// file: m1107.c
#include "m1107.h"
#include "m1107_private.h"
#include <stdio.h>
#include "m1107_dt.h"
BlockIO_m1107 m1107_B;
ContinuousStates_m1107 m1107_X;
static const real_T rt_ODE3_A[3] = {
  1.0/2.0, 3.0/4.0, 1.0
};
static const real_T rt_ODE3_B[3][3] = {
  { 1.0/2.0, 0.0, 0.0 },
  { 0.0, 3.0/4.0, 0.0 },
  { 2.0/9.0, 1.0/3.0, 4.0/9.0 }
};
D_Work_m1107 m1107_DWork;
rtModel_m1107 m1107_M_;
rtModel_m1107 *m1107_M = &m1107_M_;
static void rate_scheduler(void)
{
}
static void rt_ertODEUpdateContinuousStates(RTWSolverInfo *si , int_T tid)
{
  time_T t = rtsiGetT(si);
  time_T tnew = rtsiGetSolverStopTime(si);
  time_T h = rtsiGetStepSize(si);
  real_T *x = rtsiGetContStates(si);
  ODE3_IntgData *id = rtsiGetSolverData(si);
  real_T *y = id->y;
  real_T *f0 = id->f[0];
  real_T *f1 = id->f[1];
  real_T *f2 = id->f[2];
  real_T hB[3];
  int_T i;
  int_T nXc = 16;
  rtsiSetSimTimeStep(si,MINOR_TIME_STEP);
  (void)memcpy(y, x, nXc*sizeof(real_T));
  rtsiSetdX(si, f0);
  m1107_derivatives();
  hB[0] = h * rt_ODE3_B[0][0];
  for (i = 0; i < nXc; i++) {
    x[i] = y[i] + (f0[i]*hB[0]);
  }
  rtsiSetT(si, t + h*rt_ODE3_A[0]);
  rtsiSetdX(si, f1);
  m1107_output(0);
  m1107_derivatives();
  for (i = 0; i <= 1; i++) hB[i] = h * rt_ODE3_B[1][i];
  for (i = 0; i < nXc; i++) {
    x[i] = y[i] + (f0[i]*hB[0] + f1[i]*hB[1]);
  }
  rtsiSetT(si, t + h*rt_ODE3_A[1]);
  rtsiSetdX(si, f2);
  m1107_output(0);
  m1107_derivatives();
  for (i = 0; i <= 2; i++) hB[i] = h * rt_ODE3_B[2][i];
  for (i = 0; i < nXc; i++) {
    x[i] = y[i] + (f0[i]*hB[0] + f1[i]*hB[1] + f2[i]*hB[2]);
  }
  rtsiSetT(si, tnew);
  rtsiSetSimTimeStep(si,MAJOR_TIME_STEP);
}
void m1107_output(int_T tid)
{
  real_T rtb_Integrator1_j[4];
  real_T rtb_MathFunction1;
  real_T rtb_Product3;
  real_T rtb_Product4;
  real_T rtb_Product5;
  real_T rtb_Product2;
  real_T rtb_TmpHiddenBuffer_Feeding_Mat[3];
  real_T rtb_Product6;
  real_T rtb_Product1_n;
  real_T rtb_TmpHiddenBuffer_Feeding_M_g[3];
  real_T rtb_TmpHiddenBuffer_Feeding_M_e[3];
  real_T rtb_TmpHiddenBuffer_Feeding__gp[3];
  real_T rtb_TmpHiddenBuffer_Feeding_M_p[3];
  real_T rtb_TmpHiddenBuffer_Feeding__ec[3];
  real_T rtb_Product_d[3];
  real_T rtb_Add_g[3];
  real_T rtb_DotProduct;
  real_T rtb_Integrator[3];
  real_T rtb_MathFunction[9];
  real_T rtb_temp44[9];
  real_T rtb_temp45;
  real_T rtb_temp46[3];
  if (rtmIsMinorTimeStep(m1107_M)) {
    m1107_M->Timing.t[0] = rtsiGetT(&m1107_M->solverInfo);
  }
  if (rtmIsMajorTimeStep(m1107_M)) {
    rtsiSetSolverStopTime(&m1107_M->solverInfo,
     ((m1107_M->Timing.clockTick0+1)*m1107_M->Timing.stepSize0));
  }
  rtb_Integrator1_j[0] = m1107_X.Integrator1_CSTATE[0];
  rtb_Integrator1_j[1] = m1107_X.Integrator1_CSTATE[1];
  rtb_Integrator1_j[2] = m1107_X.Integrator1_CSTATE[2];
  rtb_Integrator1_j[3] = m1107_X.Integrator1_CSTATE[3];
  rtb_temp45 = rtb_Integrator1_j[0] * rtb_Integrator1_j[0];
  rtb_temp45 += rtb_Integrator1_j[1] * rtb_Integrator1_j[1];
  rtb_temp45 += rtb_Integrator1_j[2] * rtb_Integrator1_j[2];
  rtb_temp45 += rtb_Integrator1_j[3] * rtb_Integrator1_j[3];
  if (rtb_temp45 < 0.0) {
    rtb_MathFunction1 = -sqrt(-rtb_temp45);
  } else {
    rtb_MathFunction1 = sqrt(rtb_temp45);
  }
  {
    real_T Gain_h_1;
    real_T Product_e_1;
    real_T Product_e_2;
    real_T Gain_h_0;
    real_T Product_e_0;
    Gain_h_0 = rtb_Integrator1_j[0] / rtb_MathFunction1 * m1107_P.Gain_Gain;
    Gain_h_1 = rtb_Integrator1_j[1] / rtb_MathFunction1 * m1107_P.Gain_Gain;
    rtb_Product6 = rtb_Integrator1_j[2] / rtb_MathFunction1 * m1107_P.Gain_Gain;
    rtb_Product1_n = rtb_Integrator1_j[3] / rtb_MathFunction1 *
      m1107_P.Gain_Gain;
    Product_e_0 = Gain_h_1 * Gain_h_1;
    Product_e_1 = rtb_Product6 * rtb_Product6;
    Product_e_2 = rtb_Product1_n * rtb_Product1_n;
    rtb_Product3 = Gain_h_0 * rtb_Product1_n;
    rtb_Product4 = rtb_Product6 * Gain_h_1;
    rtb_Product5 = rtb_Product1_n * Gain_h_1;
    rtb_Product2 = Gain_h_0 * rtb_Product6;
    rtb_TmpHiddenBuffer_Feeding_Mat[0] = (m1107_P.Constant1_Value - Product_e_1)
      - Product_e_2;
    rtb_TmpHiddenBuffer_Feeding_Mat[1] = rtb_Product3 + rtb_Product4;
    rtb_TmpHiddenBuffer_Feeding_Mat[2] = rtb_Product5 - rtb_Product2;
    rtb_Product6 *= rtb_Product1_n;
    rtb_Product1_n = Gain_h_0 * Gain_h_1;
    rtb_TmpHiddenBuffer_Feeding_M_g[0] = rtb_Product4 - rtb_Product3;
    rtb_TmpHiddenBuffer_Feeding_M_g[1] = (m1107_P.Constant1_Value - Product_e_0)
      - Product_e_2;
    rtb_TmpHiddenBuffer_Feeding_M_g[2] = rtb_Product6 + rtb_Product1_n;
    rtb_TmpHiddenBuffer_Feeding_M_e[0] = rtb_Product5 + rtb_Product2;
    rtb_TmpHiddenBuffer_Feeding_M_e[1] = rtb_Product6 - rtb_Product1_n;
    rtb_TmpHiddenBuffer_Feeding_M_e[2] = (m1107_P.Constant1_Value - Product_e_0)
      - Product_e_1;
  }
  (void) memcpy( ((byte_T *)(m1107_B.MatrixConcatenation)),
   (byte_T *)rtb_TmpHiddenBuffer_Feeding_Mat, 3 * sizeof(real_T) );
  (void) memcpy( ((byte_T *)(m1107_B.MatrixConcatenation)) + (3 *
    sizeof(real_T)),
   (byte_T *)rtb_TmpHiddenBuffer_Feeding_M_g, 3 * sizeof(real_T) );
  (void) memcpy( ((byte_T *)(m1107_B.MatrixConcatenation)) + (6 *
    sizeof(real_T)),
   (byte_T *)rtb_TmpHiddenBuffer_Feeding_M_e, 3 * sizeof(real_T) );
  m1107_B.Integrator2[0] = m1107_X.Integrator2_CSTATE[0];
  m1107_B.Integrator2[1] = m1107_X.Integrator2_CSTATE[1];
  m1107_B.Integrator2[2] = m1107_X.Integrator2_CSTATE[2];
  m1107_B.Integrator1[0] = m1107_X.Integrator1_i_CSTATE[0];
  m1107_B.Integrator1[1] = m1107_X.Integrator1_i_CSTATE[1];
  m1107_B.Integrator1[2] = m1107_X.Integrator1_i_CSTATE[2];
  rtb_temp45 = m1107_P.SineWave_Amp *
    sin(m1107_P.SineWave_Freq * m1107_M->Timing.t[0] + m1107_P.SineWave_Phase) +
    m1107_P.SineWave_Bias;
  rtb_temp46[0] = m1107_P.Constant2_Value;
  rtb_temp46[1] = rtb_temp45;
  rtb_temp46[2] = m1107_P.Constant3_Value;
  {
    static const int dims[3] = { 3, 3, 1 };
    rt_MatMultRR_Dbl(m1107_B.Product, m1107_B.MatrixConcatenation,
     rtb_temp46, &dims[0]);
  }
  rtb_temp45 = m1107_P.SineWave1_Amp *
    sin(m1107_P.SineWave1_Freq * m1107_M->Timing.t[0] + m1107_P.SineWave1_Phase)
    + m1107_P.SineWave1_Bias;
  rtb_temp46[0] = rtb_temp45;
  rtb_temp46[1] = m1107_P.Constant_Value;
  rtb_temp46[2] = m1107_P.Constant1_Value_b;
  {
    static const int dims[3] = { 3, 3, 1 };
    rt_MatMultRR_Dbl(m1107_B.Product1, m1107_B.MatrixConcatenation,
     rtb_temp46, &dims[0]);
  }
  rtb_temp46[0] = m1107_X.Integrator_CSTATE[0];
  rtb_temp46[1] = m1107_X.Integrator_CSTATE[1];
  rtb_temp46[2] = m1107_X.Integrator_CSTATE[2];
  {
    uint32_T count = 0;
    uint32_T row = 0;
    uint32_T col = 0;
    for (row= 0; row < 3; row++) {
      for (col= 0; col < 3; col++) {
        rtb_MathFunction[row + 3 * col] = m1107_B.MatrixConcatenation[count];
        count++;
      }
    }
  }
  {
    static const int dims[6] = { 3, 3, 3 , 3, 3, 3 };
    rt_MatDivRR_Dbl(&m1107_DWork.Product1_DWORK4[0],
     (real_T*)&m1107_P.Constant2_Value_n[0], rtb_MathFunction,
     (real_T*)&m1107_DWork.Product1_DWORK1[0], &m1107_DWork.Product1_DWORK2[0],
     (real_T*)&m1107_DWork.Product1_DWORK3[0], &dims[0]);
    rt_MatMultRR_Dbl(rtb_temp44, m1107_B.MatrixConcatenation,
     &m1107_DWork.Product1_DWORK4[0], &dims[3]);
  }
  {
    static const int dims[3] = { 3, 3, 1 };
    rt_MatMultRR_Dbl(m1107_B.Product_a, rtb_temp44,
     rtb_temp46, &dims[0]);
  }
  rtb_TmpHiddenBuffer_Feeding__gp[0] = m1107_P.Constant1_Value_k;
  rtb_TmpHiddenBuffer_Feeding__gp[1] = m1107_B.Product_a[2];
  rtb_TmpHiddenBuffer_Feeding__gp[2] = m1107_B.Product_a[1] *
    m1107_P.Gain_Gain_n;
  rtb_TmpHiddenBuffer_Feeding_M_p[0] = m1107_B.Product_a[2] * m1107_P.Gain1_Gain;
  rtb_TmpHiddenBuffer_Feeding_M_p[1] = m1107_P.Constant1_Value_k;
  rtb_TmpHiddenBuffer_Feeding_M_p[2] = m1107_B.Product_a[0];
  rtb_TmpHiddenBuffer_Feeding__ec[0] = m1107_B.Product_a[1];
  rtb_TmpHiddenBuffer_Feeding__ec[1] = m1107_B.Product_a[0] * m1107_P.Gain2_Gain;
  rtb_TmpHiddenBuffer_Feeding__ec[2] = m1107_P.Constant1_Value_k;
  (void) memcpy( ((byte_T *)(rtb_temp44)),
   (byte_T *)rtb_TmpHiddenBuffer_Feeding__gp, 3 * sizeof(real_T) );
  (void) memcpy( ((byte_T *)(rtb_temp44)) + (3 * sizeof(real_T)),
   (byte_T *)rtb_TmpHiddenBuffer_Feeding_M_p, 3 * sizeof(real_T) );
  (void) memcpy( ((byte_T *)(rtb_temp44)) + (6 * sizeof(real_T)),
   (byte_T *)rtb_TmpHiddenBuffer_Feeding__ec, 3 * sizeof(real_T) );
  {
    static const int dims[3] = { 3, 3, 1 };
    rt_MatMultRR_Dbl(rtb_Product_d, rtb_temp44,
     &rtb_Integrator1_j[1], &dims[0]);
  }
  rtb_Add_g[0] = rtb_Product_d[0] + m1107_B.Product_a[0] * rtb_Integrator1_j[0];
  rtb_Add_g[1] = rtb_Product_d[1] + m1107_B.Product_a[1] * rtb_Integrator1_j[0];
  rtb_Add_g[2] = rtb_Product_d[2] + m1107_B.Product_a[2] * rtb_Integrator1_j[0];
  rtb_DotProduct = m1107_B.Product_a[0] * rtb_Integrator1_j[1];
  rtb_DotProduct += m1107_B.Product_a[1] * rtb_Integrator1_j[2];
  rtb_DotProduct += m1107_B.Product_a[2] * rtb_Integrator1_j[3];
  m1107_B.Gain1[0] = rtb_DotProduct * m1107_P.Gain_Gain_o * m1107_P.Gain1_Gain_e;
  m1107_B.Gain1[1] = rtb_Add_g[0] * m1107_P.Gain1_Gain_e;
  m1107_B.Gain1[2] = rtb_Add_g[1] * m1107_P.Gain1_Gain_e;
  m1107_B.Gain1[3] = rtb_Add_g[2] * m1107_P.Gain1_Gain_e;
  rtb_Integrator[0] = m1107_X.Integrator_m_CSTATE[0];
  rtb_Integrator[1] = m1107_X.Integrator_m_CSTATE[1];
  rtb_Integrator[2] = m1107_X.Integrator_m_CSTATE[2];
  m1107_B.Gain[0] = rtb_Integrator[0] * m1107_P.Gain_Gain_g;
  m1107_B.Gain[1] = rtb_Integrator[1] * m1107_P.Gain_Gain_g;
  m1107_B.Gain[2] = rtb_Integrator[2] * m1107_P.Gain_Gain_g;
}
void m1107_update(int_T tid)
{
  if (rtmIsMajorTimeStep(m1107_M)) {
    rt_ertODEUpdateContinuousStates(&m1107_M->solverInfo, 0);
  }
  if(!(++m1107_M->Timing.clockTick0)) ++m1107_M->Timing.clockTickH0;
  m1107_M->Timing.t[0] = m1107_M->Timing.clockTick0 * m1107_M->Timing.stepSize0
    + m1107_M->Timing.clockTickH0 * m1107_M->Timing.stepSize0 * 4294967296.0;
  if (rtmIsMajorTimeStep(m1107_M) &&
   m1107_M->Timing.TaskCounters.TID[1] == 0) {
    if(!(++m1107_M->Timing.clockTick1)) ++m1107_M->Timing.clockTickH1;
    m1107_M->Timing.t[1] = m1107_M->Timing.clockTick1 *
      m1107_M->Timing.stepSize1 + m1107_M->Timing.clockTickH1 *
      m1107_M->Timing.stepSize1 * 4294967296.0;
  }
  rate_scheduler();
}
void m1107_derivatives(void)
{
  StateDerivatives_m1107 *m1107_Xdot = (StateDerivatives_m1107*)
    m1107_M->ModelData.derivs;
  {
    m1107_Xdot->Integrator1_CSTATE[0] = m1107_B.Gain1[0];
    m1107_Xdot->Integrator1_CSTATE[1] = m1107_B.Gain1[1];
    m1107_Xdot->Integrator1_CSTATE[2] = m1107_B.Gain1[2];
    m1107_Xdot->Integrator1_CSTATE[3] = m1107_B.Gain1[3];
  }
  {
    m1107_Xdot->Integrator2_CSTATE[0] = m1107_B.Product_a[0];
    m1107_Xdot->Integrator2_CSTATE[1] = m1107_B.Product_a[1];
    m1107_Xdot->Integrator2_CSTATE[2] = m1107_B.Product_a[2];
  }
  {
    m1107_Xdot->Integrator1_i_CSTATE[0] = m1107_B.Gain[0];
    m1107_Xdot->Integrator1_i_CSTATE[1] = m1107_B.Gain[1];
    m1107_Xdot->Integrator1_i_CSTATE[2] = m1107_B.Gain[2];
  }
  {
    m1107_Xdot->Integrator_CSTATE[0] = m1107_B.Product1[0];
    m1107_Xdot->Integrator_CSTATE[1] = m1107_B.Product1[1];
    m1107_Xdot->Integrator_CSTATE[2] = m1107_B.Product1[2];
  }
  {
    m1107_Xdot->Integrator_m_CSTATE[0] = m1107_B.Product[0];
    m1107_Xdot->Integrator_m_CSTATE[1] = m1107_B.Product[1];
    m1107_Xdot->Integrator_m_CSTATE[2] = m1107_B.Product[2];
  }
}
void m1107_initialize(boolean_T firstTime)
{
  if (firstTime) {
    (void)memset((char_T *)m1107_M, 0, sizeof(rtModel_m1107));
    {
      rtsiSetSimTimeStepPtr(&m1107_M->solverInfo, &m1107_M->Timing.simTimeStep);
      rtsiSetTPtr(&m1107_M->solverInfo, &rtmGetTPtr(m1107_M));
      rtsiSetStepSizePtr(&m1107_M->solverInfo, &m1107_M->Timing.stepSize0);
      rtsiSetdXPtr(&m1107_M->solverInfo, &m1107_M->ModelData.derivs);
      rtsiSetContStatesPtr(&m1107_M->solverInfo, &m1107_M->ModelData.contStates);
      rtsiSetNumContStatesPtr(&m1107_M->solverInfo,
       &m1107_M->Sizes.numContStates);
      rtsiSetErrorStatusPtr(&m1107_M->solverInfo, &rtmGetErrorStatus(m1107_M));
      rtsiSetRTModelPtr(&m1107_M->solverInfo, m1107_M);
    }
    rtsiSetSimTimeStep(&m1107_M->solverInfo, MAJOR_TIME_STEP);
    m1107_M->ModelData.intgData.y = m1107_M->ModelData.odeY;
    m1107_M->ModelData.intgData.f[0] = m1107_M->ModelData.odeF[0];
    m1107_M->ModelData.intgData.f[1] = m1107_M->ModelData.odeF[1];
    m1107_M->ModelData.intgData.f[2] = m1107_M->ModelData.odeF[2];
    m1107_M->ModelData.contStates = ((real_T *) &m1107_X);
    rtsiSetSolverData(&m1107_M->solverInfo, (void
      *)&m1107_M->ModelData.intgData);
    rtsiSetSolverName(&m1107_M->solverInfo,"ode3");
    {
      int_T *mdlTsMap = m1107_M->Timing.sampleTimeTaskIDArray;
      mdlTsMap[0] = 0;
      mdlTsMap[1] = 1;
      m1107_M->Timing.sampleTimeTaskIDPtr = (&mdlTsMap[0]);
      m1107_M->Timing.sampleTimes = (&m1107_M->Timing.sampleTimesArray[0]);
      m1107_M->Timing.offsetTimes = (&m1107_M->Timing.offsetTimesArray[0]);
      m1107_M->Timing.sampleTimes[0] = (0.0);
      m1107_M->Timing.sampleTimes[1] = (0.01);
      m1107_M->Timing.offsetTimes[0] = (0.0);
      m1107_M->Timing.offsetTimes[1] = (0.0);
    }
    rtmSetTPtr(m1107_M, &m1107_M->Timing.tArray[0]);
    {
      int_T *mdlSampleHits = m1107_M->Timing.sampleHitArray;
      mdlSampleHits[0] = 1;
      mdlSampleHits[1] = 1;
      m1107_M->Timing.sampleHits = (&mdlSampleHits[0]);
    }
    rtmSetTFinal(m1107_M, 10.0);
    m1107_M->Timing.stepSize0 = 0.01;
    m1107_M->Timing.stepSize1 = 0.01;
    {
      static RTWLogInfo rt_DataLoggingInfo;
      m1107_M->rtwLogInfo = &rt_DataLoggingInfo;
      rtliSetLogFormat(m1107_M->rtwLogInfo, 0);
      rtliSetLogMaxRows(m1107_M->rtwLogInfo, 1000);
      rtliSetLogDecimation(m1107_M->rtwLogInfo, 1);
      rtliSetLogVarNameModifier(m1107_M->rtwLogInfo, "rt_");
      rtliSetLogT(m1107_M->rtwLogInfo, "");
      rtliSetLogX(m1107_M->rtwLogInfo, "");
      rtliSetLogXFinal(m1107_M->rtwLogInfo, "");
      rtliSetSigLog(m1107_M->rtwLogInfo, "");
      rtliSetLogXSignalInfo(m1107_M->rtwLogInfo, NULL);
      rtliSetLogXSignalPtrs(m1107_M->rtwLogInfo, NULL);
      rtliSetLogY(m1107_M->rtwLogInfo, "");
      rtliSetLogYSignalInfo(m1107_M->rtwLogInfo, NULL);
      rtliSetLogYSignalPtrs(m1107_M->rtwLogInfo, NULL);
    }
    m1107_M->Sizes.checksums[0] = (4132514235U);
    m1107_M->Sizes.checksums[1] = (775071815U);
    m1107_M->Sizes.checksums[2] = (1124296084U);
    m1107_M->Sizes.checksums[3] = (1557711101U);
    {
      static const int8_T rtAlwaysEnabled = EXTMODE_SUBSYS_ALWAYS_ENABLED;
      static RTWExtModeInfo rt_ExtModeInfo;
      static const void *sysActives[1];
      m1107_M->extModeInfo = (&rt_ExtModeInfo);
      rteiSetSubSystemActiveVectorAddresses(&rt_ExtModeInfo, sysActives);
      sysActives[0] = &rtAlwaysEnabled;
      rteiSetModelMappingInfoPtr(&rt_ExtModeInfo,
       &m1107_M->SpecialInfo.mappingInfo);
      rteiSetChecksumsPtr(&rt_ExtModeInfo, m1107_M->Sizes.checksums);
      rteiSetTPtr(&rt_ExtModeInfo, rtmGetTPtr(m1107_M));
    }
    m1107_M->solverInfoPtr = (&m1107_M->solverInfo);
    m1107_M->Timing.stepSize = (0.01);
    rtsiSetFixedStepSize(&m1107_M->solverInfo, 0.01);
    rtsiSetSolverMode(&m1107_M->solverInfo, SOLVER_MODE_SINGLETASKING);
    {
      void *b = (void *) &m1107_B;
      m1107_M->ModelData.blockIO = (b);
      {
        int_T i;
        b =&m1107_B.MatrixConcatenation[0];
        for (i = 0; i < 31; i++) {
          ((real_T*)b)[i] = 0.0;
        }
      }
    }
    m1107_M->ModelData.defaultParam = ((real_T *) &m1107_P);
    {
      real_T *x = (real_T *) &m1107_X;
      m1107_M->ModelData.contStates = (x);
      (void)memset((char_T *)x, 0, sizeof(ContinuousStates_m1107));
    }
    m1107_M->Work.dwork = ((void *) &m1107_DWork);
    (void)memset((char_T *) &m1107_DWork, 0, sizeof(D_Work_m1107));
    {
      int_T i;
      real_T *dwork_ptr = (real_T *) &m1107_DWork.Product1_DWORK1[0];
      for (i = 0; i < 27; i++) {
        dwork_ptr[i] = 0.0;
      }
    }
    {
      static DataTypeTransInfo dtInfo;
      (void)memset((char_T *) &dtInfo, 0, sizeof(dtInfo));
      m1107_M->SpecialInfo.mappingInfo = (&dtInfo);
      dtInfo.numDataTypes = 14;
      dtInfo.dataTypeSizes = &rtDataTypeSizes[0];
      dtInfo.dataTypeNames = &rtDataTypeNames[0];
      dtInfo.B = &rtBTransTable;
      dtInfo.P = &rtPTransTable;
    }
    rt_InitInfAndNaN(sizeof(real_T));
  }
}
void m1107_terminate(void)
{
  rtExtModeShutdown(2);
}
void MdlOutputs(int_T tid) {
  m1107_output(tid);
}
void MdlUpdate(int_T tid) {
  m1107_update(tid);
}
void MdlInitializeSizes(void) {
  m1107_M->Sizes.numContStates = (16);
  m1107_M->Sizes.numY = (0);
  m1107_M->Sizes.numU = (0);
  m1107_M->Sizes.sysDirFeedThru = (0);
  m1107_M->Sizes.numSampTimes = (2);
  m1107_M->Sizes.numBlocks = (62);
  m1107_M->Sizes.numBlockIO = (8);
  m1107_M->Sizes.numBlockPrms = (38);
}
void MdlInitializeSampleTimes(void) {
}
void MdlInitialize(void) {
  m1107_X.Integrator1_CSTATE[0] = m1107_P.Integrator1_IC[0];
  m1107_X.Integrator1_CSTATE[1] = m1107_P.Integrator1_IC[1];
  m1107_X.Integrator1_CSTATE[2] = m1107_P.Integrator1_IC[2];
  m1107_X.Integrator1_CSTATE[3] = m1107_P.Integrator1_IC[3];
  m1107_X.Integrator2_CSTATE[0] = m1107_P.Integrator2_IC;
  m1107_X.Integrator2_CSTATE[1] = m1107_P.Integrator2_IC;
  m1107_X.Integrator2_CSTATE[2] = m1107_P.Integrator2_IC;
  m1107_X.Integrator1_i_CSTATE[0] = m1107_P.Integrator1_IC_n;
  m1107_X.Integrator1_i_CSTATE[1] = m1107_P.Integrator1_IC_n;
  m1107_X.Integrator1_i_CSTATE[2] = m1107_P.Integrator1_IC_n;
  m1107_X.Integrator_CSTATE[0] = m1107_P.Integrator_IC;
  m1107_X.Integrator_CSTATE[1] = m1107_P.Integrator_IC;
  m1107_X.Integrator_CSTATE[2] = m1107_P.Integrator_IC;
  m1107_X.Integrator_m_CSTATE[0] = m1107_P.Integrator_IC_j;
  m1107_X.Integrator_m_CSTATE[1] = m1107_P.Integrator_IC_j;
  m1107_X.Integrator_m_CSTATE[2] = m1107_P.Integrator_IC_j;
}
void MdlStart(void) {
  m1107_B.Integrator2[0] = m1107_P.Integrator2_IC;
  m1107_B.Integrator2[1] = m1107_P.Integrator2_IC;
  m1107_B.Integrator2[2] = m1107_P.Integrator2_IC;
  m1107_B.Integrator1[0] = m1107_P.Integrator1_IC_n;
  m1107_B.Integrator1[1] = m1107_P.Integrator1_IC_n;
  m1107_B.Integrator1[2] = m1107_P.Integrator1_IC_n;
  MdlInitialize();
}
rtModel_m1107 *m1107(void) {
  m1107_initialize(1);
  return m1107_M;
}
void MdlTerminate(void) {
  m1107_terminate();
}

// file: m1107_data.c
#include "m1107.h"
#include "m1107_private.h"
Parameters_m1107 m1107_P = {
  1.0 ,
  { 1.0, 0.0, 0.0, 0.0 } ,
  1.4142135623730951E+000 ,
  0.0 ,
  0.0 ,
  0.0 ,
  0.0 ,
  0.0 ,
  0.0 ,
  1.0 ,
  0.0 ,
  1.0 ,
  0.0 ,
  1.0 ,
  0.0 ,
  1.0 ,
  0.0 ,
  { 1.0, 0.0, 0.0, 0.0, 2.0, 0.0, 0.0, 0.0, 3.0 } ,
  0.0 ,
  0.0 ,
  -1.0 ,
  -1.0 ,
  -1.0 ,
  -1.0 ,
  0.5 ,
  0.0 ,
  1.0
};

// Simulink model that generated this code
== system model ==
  Integrator1 : Integrator  <- 1: Gain
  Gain : Gain  <- 1: Integrator
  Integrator : Integrator  <- 1: Product
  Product : Product  Multiplication=Matrix(*)  <- 1: MatrixConcatenation, 2: Reshape#1
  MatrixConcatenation : simulink/Math Operations/Matrix Concatenation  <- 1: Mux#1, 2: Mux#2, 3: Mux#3
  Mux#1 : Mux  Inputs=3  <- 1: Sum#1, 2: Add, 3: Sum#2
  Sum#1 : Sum  Inputs=+--  <- 1: Constant1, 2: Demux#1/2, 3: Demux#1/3
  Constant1 : Constant
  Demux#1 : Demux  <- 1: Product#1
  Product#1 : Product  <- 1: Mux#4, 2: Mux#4
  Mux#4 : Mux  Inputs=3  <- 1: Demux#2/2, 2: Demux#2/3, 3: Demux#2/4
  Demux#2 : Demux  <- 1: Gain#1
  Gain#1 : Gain  Gain=sqrt(2)  <- 1: Product#2
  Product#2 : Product  Inputs=*/  <- 1: Integrator#1, 2: MathFunction1
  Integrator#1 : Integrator  InitialCondition=[1;0;0;0]  <- 1: Gain1
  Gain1 : Gain  Gain=0.5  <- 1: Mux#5
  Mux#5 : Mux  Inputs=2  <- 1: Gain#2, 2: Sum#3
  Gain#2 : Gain  Gain=-1  <- 1: DotProduct
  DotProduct : simulink/Math Operations/Dot Product  <- 1: Product#3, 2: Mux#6
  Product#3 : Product  Multiplication=Matrix(*)  <- 1: Product1, 2: Integrator#2
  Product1 : Product  Inputs=*/*  Multiplication=Matrix(*)  <- 1: MatrixConcatenation, 2: Constant2, 3: MathFunction
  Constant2 : Constant  Value=[1,0,0;0,2,0;0,0,3]
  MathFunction : Math  Operator=transpose  <- 1: MatrixConcatenation
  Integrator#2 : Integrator  <- 1: Product#4
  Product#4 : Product  Multiplication=Matrix(*)  <- 1: MatrixConcatenation, 2: Reshape#2
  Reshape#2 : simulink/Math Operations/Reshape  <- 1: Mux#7
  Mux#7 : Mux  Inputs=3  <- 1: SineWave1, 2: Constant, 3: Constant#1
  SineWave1 : Sin
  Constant : Constant  Value=0
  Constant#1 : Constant  Value=0
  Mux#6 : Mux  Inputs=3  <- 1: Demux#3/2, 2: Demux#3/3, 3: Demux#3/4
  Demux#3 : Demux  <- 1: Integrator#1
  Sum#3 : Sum  <- 1: Product#5, 2: Product#6
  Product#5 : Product  Multiplication=Matrix(*)  <- 1: MatrixConcatenation#1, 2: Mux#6
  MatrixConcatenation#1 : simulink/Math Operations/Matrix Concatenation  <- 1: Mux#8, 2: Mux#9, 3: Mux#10
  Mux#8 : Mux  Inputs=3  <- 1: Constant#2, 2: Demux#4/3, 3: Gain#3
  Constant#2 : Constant  Value=0
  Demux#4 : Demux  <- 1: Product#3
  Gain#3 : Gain  Gain=-1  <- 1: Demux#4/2
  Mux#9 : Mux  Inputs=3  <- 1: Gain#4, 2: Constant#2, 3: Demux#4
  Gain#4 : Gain  Gain=-1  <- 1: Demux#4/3
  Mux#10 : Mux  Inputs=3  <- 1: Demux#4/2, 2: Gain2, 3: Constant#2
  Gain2 : Gain  Gain=-1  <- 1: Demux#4
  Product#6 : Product  <- 1: Product#3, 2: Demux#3
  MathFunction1 : Math  Operator=sqrt  <- 1: DotProduct#1
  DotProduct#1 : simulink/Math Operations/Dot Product  <- 1: Integrator#1, 2: Integrator#1
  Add : Sum  <- 1: Product3, 2: Product4
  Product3 : Product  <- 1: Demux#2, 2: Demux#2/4
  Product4 : Product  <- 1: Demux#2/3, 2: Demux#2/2
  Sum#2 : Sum  Inputs=+-  <- 1: Product5, 2: Product2
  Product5 : Product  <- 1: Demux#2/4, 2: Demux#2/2
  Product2 : Product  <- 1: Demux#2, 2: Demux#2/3
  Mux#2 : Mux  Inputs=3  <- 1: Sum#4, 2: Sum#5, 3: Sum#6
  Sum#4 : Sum  Inputs=+-  <- 1: Product4, 2: Product3
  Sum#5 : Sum  Inputs=+--  <- 1: Constant1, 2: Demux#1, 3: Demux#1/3
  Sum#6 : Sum  <- 1: Product6, 2: Product#7
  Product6 : Product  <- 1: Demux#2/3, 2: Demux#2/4
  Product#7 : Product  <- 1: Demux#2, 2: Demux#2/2
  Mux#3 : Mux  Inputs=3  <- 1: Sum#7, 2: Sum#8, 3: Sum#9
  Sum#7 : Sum  <- 1: Product5, 2: Product2
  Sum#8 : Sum  Inputs=+-  <- 1: Product6, 2: Product#7
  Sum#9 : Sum  Inputs=+--  <- 1: Constant1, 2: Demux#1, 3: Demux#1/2
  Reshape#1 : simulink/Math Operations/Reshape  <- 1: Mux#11
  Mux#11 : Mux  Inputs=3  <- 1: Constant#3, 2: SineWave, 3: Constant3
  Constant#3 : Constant  Value=0
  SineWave : Sin
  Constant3 : Constant  Value=0
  Integrator2 : Integrator  <- 1: Product#3
